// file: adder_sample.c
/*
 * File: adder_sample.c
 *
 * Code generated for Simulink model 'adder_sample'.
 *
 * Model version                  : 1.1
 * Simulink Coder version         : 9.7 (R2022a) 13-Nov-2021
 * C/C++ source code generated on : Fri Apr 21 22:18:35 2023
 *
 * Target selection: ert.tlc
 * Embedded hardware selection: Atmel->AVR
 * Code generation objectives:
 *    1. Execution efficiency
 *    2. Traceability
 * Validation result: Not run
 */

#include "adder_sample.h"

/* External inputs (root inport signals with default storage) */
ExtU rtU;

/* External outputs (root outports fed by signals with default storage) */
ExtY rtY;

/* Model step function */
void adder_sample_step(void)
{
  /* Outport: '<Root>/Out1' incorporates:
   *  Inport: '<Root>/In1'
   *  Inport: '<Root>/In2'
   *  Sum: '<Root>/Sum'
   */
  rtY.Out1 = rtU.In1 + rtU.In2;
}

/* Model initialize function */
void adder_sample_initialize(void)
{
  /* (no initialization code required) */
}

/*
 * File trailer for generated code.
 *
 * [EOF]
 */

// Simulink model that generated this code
simulink model "adder_sample"  (R2022a)
settings: Solver=FixedStepDiscrete  StartTime=0.0  StopTime=10.0  RelTol=1e-3  EnableMultiTasking=on
model workspace (MATLAB code in the model file):
  | cmdLim = Simulink.Parameter;
  | cmdLim.Value = 15;
  | cmdLim.Description = 'Limit for controlling the maximum surface command angle.';
  | cmdLim.Min = 0;
  | cmdLim.Max = 90;
  | cmdLim.DocUnits = 'deg';
  | 
  | dispGain = Simulink.Parameter;
  | dispGain.Value = 0.75;
  | dispGain.Description = 'Gain applied to the displacement error.';
  | dispGain.Min = 0;
  | dispGain.Max = [];
  | dispGain.DocUnits = 'deg/sec/deg';
  | 
  | dispLim = Simulink.Parameter;
  | dispLim.Value = 30;
  | dispLim.Description = 'Limit for controlling the maximum commanded angle.';
  | dispLim.Min = 0;
  | dispLim.Max = 180;
  | dispLim.DocUnits = 'deg';
  | 
  | intGain = Simulink.Parameter;
  | intGain.Value = 0.5;
  | intGain.Description = 'Gain applied to the integral error.';
  | intGain.Min = 0;
  | intGain.Max = [];
  | intGain.DocUnits = 'deg/sec/deg/sec';
  | 
  | intLim = Simulink.Parameter;
  | intLim.Value = 5;
  | intLim.Description = 'Limit for controlling the maximum commanded angle.';
  | intLim.Min = 0;
  | intLim.Max = 90;
  | intLim.DocUnits = 'deg';
  | 
  | rateGain = Simulink.Parameter;
  | rateGain.Value = 2;
  | rateGain.Description = 'Gain applied to the rate error.';
  | rateGain.Min = 0;
  | rateGain.Max = [];
  | rateGain.DocUnits = 'deg/deg/sec';
  | 
  | rateLim = Simulink.Parameter;
  | rateLim.Value = 6;
  | rateLim.Description = 'Limit for controlling the maximum commanded angle.';
  | rateLim.Min = 0;
  | rateLim.Max = 180;
  | rateLim.DocUnits = 'deg/sec';
  | 
  | hdgGain = Simulink.Parameter;
  | hdgGain.Value = 0.015;

== system adder_sample ==
  In1 : Inport  OutDataTypeStr=single
  In2 : Inport  Port=2  OutDataTypeStr=single
  Sum : Sum  Inputs=|++  InputSameDT=on  OutDataTypeStr=Inherit: Same as first input
  Out1 : Outport  VectorParamsAs1DForOutWhenUnconnected=off
  wires:
  In1/1 -> Sum/1
  In2/1 -> Sum/2
  Sum/1 -> Out1/1
